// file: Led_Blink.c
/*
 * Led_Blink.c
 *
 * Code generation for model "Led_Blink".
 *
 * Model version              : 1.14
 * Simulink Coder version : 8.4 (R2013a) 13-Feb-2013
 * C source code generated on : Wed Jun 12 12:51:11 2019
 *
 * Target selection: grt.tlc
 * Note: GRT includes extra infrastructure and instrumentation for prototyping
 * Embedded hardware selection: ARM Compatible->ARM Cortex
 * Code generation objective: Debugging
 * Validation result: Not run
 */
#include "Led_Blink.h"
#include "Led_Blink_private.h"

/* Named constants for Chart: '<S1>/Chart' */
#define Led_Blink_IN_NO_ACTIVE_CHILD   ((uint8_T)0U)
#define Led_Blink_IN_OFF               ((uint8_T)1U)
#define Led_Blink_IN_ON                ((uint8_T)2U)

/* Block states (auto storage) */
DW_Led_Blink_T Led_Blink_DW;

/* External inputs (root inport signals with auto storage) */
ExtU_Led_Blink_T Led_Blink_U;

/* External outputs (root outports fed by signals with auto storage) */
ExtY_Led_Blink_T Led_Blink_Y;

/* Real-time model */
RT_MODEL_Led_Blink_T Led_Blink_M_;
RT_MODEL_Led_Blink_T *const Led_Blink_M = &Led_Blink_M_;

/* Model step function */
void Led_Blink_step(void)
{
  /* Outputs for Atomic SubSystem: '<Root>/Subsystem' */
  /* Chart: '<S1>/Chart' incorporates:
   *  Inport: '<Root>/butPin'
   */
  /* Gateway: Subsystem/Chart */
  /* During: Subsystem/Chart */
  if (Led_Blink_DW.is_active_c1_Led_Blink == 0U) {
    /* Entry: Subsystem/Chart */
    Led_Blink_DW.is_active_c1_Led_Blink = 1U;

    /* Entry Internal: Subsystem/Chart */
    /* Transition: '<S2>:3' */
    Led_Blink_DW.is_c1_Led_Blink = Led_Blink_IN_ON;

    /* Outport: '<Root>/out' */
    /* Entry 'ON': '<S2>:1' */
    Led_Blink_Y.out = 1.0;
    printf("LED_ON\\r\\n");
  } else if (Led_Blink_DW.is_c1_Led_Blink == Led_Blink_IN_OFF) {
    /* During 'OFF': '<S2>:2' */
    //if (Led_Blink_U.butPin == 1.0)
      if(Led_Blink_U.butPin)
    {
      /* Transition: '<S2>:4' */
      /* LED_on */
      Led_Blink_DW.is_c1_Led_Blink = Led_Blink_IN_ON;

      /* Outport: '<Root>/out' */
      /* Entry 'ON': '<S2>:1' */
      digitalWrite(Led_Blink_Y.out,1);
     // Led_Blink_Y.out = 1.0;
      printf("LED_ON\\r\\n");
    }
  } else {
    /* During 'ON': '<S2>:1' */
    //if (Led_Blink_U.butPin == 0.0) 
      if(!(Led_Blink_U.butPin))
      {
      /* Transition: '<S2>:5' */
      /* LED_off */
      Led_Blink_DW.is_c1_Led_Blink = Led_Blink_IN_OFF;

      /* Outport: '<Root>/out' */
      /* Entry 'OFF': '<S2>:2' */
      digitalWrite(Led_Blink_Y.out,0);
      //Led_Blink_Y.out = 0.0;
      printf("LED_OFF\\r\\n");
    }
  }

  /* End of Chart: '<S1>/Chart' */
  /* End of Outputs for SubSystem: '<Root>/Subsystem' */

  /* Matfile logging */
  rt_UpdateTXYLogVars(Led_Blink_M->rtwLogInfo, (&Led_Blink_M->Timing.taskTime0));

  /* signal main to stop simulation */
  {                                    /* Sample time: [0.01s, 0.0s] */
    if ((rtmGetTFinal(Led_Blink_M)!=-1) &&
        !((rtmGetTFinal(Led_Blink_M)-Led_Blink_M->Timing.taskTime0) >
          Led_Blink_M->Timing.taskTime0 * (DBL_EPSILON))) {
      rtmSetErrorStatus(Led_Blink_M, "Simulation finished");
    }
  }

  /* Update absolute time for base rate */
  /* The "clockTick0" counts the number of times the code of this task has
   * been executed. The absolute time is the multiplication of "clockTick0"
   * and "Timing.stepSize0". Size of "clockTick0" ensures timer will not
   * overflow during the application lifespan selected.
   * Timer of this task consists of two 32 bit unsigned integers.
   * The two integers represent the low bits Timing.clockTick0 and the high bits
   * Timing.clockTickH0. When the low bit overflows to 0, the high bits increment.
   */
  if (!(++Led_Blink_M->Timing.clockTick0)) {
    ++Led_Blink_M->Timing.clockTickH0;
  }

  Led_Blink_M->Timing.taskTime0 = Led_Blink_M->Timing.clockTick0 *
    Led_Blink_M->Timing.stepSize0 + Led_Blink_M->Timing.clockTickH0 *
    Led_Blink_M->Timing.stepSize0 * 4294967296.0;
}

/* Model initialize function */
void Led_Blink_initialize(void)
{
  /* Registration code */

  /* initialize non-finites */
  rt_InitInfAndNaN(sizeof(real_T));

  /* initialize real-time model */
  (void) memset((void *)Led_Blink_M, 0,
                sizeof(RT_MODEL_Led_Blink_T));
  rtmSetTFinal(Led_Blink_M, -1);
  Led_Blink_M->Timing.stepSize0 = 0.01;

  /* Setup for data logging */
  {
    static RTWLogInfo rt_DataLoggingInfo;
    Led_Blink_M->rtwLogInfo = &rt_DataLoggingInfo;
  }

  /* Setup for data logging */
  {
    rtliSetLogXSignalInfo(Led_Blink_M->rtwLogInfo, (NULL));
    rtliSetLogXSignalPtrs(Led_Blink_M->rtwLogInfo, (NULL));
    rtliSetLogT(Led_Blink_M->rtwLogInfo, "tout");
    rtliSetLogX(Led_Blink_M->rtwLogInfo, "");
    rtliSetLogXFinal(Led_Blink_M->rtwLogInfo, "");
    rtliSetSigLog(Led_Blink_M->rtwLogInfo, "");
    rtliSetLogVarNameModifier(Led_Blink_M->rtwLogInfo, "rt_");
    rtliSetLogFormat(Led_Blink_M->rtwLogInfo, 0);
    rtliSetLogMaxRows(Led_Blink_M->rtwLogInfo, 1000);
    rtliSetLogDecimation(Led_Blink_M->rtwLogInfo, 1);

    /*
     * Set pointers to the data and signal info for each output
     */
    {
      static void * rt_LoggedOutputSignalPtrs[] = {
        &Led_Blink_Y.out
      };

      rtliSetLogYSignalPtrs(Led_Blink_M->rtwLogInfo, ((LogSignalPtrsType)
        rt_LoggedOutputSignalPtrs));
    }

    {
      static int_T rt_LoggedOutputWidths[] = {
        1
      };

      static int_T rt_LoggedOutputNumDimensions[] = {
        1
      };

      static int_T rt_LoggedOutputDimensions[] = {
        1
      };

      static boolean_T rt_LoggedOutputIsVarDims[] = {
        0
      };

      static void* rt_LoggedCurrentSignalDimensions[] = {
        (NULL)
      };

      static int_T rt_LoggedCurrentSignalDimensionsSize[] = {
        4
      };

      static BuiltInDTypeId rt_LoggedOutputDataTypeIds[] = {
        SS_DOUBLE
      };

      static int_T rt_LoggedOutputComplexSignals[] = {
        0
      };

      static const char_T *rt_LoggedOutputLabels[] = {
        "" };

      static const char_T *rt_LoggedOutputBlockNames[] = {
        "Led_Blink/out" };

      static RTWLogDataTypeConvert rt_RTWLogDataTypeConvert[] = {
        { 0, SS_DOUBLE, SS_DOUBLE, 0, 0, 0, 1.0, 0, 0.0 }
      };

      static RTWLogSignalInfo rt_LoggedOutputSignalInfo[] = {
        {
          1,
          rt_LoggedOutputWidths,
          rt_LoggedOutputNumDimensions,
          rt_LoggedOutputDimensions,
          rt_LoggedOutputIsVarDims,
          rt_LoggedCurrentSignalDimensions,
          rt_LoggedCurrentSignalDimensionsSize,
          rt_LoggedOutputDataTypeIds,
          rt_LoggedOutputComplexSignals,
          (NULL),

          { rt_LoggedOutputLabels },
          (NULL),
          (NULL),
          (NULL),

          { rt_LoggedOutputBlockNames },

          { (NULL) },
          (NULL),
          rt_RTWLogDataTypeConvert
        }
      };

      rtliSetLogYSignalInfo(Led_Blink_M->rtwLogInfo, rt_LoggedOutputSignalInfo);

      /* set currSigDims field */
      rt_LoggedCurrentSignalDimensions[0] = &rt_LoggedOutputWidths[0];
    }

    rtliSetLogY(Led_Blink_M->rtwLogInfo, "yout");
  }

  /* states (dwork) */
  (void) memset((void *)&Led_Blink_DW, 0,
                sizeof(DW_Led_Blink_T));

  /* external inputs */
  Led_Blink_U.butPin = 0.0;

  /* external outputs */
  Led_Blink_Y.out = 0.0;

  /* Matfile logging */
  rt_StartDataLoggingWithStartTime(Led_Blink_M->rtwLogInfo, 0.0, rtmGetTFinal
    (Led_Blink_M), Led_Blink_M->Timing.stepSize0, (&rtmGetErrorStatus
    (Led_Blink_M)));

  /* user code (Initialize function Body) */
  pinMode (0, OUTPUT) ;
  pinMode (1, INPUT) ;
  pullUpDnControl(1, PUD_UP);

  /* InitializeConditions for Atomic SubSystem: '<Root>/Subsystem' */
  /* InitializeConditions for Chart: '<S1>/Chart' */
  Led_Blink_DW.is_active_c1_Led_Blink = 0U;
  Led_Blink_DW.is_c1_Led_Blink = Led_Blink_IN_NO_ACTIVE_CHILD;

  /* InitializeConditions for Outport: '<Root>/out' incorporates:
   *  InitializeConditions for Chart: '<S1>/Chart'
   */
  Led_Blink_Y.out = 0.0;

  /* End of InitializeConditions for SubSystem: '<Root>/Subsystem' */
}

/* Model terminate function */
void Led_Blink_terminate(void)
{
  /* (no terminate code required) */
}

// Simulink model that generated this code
simulink model "Led_Blink"  (R2013a)
settings: Solver=FixedStepDiscrete  StartTime=0.0  StopTime=inf  FixedStep=0.01  RelTol=1e-3

== system Led_Blink ==
  butPin : Inport
  Subsystem : Subsystem  TreatAsAtomicUnit=on
  out : Outport
  wires:
  butPin/1 -> Subsystem/1(SW)
  Subsystem/1(out) -> out/1

== system Led_Blink/Subsystem ==
  SW : Inport
  Chart : Stateflow chart  TreatAsAtomicUnit=on
  out : Outport
  wires:
  Chart/1(out) -> out/1
  SW/1 -> Chart/1(SW)

== stateflow chart Led_Blink/Subsystem/Chart ==
  state OFF
    en: out=0;
    printf("LED_OFF\r\n");
  state ON
    en: out =1;
    printf("LED_ON\r\n");
  (default) -> ON
  OFF -> ON : [SW==1]
      | /*LED_on*/
  ON -> OFF : [SW==0]
      | /*LED_off*/
  data: SW input; out output double
